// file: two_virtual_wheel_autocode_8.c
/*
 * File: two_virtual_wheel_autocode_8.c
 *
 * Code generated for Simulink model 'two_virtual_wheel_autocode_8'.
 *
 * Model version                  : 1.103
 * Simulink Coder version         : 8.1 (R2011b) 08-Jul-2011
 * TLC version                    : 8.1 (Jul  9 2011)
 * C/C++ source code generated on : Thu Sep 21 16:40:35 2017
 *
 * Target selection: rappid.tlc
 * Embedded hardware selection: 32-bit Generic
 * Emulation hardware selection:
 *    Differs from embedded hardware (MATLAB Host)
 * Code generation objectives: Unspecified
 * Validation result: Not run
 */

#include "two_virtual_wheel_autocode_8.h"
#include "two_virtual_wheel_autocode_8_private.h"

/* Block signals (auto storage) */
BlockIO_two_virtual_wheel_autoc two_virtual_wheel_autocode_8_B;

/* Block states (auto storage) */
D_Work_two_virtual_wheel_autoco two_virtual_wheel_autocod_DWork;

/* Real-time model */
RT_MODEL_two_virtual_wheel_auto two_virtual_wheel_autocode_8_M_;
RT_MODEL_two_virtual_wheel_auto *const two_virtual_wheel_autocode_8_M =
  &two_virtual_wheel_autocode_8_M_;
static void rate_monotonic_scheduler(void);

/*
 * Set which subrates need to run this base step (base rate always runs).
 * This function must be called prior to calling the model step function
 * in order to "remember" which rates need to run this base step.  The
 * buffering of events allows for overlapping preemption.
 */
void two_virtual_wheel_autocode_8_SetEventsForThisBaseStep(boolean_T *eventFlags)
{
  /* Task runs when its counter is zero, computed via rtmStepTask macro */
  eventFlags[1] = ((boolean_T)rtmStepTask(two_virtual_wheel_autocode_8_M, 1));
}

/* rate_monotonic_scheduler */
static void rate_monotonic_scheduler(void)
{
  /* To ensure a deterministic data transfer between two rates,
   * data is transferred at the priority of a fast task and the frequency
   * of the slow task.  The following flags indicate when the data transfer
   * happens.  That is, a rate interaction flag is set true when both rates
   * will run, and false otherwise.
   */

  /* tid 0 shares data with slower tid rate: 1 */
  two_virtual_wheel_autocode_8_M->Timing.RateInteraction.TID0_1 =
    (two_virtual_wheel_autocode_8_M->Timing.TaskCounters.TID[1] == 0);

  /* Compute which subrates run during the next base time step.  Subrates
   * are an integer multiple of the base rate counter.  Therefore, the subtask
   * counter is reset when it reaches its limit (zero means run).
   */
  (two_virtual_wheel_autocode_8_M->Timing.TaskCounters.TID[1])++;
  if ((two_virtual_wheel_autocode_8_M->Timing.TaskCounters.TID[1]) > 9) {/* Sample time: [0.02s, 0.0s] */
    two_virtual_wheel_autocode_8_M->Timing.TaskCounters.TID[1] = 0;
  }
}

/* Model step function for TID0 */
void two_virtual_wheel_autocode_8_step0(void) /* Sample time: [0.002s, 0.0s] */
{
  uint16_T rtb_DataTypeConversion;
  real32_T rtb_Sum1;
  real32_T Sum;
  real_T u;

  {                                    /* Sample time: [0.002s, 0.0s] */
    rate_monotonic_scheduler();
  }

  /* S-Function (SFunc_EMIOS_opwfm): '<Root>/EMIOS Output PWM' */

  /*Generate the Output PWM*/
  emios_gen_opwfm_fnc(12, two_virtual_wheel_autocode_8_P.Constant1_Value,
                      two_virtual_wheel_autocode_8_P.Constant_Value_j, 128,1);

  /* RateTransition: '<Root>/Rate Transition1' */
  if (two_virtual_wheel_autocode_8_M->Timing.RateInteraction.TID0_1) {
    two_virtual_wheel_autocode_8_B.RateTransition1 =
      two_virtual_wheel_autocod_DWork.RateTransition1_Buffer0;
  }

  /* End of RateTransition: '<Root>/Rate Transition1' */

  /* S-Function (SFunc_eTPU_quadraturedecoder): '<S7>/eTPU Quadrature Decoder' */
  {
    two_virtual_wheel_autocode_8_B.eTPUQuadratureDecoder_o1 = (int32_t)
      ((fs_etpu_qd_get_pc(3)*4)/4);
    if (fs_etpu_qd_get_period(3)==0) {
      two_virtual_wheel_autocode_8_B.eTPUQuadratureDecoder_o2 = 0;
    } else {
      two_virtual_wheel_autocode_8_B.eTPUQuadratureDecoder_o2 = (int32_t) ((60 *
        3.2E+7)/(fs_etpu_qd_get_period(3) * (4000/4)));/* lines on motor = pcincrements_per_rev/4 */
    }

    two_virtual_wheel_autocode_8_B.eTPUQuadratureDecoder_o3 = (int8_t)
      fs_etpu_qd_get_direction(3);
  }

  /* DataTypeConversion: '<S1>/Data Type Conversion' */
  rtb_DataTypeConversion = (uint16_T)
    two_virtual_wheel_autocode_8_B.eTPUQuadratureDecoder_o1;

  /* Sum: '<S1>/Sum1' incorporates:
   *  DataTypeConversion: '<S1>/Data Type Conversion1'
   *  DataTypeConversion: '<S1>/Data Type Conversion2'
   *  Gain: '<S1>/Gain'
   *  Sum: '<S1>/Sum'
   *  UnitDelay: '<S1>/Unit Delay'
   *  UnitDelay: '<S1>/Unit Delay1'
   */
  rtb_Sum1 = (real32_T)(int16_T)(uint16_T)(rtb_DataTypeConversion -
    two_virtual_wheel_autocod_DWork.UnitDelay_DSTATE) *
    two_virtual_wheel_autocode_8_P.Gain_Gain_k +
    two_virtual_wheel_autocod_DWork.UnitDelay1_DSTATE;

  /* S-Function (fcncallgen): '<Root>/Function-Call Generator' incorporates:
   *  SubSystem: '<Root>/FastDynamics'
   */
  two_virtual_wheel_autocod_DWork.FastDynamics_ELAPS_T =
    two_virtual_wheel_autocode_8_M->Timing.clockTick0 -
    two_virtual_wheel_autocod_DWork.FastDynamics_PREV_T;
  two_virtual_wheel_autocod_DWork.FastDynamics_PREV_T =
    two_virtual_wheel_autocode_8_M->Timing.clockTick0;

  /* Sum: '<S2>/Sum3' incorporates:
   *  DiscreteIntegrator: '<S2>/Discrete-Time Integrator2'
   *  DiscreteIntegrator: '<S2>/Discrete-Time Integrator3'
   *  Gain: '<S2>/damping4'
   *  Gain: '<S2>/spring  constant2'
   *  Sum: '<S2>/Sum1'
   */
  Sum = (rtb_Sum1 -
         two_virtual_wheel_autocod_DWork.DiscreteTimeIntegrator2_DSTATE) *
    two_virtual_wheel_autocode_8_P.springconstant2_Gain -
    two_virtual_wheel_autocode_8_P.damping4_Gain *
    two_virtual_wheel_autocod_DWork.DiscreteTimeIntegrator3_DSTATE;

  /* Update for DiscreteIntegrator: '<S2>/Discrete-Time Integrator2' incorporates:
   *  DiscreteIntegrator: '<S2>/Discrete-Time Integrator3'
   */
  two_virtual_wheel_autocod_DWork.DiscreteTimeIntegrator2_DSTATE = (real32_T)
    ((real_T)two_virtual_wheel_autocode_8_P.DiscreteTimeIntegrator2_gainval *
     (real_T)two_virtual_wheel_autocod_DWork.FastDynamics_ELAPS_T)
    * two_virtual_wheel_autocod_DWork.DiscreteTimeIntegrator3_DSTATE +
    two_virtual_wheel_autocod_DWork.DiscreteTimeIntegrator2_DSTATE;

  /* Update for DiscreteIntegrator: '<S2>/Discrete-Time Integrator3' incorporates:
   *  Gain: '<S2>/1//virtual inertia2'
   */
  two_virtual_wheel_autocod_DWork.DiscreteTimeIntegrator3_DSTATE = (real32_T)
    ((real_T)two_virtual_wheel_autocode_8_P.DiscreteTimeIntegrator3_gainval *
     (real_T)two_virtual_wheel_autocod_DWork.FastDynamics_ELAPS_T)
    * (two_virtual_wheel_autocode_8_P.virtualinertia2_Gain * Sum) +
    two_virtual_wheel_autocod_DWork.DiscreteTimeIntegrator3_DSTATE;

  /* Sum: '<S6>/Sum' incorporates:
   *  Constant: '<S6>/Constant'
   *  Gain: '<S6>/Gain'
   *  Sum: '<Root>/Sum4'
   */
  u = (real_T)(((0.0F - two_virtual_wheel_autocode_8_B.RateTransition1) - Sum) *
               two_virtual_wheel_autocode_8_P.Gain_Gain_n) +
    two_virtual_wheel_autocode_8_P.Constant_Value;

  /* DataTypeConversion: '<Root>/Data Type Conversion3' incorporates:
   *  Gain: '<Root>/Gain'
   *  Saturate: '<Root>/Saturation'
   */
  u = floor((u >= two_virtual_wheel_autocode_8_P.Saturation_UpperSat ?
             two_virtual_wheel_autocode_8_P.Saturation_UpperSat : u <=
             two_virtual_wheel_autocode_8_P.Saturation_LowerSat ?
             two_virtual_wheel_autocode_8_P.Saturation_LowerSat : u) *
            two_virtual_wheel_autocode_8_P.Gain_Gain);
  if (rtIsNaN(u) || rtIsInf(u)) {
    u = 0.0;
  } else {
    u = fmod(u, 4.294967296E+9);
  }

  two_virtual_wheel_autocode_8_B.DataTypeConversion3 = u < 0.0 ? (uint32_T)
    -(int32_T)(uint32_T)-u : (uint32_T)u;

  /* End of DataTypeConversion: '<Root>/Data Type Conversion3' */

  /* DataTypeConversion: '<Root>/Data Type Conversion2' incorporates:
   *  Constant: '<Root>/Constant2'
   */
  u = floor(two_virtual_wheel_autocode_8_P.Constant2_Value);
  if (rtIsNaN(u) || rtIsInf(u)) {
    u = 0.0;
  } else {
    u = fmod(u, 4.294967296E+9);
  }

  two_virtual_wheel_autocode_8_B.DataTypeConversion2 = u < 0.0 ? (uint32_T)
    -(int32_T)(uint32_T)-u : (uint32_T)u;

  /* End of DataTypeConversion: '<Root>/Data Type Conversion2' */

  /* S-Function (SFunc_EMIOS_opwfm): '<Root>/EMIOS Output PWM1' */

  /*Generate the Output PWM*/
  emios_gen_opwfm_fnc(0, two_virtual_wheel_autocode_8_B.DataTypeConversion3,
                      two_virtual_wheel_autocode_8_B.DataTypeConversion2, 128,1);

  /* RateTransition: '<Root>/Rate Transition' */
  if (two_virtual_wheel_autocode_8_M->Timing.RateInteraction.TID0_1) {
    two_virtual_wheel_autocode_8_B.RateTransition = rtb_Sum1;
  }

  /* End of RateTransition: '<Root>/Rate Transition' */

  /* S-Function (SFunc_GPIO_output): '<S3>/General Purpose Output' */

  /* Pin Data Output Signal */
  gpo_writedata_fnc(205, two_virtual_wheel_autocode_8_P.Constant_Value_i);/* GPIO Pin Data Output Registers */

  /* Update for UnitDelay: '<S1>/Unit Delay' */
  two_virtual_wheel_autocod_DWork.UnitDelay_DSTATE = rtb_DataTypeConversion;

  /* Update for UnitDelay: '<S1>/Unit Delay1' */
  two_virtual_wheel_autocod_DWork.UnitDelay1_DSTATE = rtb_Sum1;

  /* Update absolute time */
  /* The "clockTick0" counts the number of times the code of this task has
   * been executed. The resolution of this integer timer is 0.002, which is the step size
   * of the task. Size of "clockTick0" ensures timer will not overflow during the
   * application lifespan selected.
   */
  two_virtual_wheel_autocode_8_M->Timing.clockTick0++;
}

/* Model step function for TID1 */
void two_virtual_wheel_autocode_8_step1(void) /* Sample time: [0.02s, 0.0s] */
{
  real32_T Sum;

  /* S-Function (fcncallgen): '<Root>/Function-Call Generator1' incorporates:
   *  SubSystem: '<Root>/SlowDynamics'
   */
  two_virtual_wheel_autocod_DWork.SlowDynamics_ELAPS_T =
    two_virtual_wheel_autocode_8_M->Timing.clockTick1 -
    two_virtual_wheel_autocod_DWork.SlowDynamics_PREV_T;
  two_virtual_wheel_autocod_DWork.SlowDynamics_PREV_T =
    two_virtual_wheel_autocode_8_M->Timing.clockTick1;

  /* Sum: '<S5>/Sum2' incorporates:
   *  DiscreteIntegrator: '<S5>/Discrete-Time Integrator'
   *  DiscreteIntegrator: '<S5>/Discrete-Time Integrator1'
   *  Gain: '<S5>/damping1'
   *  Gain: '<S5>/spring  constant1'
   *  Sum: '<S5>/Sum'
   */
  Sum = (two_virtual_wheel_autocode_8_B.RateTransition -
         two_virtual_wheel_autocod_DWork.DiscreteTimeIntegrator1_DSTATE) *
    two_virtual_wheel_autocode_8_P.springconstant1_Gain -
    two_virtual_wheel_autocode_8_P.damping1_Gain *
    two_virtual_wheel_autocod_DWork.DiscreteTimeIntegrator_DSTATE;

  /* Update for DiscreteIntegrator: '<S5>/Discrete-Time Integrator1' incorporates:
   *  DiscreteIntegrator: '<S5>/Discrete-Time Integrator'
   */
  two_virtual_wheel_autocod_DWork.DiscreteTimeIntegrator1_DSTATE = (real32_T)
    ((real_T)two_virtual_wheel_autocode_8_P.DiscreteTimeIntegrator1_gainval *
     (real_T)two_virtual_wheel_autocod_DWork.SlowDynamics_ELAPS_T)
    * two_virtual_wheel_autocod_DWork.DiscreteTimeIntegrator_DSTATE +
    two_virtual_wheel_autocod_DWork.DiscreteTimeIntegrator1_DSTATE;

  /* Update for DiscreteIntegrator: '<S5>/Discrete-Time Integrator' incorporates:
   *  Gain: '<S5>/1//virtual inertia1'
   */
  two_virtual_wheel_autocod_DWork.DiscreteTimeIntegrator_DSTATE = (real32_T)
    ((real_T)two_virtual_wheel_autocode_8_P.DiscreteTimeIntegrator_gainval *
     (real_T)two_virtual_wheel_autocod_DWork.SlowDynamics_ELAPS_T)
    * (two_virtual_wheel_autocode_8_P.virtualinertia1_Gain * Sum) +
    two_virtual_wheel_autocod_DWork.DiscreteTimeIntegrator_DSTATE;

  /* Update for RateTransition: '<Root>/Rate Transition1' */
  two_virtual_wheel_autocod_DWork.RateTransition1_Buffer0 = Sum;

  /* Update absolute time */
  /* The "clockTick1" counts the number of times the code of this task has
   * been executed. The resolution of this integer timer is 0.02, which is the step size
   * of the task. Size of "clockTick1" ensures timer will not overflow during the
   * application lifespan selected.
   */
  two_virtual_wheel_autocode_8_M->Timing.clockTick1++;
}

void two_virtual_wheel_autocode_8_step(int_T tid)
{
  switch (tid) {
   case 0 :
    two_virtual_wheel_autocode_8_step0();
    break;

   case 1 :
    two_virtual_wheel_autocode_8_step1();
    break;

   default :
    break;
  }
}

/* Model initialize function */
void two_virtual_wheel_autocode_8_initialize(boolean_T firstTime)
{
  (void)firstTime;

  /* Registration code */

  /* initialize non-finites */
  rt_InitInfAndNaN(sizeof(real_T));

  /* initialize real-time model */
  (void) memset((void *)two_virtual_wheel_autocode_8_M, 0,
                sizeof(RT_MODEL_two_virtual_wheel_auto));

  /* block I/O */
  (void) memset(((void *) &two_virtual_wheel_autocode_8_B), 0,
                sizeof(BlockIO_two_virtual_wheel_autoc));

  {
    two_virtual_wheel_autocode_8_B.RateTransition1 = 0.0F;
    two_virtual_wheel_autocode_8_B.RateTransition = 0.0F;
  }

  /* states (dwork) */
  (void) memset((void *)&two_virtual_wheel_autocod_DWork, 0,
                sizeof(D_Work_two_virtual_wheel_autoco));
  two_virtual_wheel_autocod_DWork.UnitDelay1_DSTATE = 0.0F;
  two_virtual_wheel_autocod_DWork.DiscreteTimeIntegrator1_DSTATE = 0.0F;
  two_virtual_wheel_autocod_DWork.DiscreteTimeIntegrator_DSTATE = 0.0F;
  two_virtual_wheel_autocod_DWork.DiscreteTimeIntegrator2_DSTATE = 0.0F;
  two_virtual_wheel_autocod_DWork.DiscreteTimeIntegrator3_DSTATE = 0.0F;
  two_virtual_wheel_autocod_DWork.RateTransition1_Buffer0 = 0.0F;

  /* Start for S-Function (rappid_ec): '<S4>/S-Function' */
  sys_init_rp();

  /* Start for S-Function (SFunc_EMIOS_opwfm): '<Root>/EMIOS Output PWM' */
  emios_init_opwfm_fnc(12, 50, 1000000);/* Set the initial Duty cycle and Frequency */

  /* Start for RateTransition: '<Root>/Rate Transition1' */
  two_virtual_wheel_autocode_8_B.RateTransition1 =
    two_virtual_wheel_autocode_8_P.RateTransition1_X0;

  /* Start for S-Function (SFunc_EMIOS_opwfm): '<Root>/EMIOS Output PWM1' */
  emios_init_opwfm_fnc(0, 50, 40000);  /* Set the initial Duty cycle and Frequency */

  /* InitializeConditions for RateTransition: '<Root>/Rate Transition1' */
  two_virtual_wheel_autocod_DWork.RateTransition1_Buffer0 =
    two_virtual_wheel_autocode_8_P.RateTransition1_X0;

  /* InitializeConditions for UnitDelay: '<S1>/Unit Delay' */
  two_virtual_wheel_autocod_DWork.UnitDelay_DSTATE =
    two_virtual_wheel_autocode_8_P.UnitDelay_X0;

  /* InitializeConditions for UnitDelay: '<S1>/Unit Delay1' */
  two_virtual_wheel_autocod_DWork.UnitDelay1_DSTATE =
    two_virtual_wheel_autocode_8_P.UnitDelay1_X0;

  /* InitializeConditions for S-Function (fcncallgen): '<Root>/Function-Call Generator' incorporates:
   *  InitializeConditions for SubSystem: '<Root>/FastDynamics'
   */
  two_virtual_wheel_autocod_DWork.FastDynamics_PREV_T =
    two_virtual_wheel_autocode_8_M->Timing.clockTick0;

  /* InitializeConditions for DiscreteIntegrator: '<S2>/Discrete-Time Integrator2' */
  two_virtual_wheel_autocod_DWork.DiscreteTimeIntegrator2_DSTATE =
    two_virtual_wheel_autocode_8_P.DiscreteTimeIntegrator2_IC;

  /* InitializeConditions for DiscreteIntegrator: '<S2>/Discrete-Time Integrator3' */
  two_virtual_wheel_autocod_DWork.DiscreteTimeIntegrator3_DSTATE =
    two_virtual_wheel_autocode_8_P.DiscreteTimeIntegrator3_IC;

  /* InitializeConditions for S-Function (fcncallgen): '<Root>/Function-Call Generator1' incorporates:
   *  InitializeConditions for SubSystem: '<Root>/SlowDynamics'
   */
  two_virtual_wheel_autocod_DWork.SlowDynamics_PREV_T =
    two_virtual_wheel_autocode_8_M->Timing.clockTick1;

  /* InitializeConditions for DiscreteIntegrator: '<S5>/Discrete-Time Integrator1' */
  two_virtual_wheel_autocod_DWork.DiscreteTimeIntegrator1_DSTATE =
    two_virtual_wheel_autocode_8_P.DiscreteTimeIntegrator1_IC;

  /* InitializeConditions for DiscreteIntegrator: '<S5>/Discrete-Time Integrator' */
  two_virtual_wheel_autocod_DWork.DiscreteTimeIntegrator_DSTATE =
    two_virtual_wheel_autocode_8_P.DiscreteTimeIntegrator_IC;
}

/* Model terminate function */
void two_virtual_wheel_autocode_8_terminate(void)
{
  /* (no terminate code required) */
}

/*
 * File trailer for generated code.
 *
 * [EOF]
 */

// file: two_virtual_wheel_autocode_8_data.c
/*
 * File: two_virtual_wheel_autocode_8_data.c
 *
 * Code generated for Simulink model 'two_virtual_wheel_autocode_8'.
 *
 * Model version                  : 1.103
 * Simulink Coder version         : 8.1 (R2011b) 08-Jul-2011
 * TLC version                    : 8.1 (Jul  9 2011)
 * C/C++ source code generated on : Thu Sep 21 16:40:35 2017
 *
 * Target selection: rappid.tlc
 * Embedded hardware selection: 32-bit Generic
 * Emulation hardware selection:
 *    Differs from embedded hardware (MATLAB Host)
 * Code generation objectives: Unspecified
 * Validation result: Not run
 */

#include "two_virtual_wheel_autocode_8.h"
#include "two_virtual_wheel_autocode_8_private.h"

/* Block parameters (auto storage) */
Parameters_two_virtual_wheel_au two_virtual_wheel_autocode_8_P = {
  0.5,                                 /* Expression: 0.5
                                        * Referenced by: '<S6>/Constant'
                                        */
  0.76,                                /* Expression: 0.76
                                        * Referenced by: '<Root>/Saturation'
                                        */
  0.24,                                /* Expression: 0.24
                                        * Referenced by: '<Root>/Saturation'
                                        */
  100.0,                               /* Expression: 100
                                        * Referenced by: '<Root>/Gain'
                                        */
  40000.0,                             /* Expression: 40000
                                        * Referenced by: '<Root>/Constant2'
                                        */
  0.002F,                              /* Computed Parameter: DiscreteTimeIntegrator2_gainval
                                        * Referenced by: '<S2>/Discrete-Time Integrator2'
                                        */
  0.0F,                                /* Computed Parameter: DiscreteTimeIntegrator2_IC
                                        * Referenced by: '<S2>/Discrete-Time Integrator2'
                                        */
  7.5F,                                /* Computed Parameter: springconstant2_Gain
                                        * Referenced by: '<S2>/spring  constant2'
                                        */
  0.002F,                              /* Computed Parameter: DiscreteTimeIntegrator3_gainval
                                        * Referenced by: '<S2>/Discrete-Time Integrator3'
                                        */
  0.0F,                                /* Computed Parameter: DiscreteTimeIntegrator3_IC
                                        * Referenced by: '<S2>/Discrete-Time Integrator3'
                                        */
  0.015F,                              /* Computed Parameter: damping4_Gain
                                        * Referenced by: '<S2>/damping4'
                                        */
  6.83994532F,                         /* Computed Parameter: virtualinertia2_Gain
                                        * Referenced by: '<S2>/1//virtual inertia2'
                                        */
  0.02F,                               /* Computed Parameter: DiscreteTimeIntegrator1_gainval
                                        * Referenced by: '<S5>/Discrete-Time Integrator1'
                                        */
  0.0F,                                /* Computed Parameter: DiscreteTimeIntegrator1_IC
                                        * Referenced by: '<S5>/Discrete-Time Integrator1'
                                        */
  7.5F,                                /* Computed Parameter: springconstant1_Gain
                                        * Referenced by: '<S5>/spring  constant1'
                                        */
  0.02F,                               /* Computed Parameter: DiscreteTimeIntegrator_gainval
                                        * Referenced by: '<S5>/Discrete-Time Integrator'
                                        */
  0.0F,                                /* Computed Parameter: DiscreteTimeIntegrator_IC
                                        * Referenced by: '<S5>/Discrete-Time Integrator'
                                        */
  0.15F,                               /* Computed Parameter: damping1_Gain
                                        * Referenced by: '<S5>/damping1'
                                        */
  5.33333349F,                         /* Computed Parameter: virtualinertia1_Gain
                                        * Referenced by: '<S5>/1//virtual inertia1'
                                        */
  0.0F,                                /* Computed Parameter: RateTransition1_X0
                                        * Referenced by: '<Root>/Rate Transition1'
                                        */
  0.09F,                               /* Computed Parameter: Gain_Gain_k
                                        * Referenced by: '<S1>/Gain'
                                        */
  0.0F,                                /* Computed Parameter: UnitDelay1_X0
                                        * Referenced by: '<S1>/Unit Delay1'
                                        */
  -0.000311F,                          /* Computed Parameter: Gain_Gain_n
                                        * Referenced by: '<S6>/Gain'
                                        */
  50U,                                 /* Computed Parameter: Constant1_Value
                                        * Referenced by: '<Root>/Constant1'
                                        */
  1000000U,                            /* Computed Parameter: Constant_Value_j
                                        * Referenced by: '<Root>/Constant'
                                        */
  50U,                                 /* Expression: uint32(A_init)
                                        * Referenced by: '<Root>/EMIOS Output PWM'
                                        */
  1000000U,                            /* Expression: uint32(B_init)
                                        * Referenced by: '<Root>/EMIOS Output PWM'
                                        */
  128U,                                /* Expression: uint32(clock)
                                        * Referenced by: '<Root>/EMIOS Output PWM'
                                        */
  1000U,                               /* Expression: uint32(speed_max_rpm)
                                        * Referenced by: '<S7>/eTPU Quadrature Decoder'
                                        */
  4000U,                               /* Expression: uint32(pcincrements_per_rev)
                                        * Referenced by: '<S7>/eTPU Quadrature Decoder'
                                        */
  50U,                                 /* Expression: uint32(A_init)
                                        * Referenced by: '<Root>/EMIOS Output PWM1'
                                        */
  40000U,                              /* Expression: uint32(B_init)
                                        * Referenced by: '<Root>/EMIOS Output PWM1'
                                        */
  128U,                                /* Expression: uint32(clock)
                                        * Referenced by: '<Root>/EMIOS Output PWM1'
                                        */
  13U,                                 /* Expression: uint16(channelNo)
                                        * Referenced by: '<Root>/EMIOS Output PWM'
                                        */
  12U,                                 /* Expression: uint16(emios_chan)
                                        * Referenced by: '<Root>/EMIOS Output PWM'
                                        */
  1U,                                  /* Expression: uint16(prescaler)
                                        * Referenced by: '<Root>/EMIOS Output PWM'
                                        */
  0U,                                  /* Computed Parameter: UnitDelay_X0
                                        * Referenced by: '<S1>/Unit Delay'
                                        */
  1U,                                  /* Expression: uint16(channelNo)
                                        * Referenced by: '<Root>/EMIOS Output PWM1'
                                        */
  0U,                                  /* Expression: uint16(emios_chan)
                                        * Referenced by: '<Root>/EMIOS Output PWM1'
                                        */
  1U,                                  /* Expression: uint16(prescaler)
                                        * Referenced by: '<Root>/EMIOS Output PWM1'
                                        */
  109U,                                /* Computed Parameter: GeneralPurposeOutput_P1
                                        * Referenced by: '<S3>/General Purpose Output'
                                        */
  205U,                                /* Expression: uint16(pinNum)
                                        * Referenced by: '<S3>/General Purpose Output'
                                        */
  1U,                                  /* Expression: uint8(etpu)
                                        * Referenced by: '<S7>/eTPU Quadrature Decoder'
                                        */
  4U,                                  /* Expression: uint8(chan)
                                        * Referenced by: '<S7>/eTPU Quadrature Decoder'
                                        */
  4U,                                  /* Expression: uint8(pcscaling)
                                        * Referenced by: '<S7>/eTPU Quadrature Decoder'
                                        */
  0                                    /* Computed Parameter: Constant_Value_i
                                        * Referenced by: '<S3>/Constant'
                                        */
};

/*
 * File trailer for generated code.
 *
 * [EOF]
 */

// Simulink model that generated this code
simulink model "two_virtual_wheel_autocode_8"  (Simulink 7.8)
settings: Solver=FixedStepDiscrete  SolverMode=MultiTasking  StartTime=0.0  StopTime=tfinal  RelTol=1e-3
InitFcn:
  | two_virtual_wheel_params
undefined symbols (not defined in the file): b1, b2, DiscIntNeverNeededParam, Jw1, Jw2, k1, k2, SFunc_eTPU_quadraturedecoder_Script, SFunc_gpio_output_Script
libraries: rappid_ec_lib x2, simulink x2, rappid_lib x1

== system two_virtual_wheel_autocode_8 ==
  note: wheel position
  note: thetaz
  Constant : Constant  Value=1000000  OutDataTypeStr=uint32
  Constant1 : Constant  Value=50  OutDataTypeStr=uint32
  Constant2 : Constant  Value=40000
  ConversionSystem : Subsystem
  Data Type Conversion{,1..3} (4 alike) : DataTypeConversion  OutDataTypeStr=uint32
  EMIOS Output PWM : rappid_ec_lib/Peripheral Driver Blocks/eMIOS Blocks/EMIOS Output PWM  channelNo=12  emios_chan=12  A_init=50  B_init=1000000  clock=128  prescaler=1
  EMIOS Output PWM1 : rappid_ec_lib/Peripheral Driver Blocks/eMIOS Blocks/EMIOS Output PWM  channelNo=0  emios_chan=0  A_init=50  B_init=40000  clock=128  prescaler=1
  FastDynamics : Subsystem
  Function-Call Generator : simulink/Ports & Subsystems/Function-Call Generator  sample_time=0.002  numberOfIterations=1
  Function-Call Generator1 : simulink/Ports & Subsystems/Function-Call Generator  sample_time=0.02  numberOfIterations=1
  GPIO Blocks : Subsystem  AncestorBlock=rappid_ec_lib/Peripheral Driver Blocks/GPIO Blocks
  Gain : Gain  Gain=100
  RAppID-EC : rappid_lib/RAppID Initialization Blocks/RAppID-EC  Tag=RAppID  Priority=0  rtos=simpletarget  targetmcu=IntRAM  clockfrequency=128  basetaskpriority=20  systemcounter=0  systimer_isrpriority=1  systimer_period=0  isrstacksize=50  interruptdispatcher=None  stored_mdl_name=two_virtual_wheel_autocode_8
  Rate Transition : RateTransition
  Rate Transition1 : RateTransition
  Saturation : Saturate  UpperLimit=0.76  LowerLimit=0.24
  SlowDynamics : Subsystem
  Subsystem : Subsystem
  Sum4 : Sum  Inputs=-|-  SaturateOnIntegerOverflow=on  InputSameDT=on  OutDataTypeStr=Inherit: Same as first input
  Terminator : Terminator
  Terminator1 : Terminator
  eTPU Blocks : Subsystem  AncestorBlock=rappid_ec_lib/Peripheral Driver Blocks/eTPU Blocks
  wires:
  ConversionSystem/1(Out1) -> Rate Transition/1, FastDynamics/1(In1)
  Rate Transition1/1 -> Sum4/1
  Rate Transition/1 -> SlowDynamics/1(thetaz)
  SlowDynamics/1(torque1) -> Rate Transition1/1
  FastDynamics/1(torque2) -> Sum4/2
  Function-Call Generator1/1 -> SlowDynamics/Trigger
  Function-Call Generator/1 -> FastDynamics/Trigger
  Constant1/1 -> Data Type Conversion/1
  Data Type Conversion/1 -> EMIOS Output PWM/1
  Constant/1 -> Data Type Conversion1/1
  Data Type Conversion1/1 -> EMIOS Output PWM/2
  Subsystem/1(Out1) -> Saturation/1
  Saturation/1 -> Gain/1
  Constant2/1 -> Data Type Conversion2/1
  Data Type Conversion2/1 -> EMIOS Output PWM1/2
  Data Type Conversion3/1 -> EMIOS Output PWM1/1
  Gain/1 -> Data Type Conversion3/1
  Sum4/1 -> Subsystem/1(In1)
  eTPU Blocks/2(Out2) -> Terminator/1
  eTPU Blocks/3(Out3) -> Terminator1/1
  eTPU Blocks/1(Out1) -> ConversionSystem/1(In1)

== system two_virtual_wheel_autocode_8/ConversionSystem ==
  In1 : Inport
  Data Type Conversion : DataTypeConversion  OutDataTypeStr=uint16
  Data Type Conversion1 : DataTypeConversion  OutDataTypeStr=single
  Data Type Conversion2 : DataTypeConversion  OutDataTypeStr=int16
  Gain : Gain  Gain=0.09
  Sum : Sum  Inputs=|+-
  Sum1 : Sum  Inputs=|++  AccumDataTypeStr=single  OutDataTypeStr=single
  Unit Delay : UnitDelay  SampleTime=-1
  Unit Delay1 : UnitDelay  SampleTime=-1
  Out1 : Outport
  wires:
  Unit Delay/1 -> Sum/2
  Sum/1 -> Data Type Conversion2/1
  Data Type Conversion2/1 -> Data Type Conversion1/1
  Data Type Conversion1/1 -> Gain/1
  Gain/1 -> Sum1/1
  Sum1/1 -> Out1/1, Unit Delay1/1
  Data Type Conversion/1 -> Sum/1, Unit Delay/1
  In1/1 -> Data Type Conversion/1
  Unit Delay1/1 -> Sum1/2

== system two_virtual_wheel_autocode_8/FastDynamics ==
  note: Fast Dynamics
  note: thetaz
  note: theta2ddot
  note: theta2dot
  note: theta2
  In1 : Inport
  Trigger : TriggerPort  TriggerType=function-call  PortDimensions=1
  1/virtual inertia2 : Gain  Gain=1/Jw2  SaturateOnIntegerOverflow=on  OutDataTypeStr=Inherit: Same as input  ParamDataTypeStr=Inherit: Same as input
  Discrete-Time Integrator2 : DiscreteIntegrator  SampleTime=-1  ICPrevOutput=DiscIntNeverNeededParam  ICPrevScaledInput=DiscIntNeverNeededParam
  Discrete-Time Integrator3 : DiscreteIntegrator  SampleTime=-1  ICPrevOutput=DiscIntNeverNeededParam  ICPrevScaledInput=DiscIntNeverNeededParam
  Sum1 : Sum  Inputs=|+-  SaturateOnIntegerOverflow=on  InputSameDT=on  OutDataTypeStr=Inherit: Same as first input
  Sum3 : Sum  Inputs=|+-  SaturateOnIntegerOverflow=on  InputSameDT=on  OutDataTypeStr=Inherit: Same as first input
  damping4 : Gain  Gain=b2  SaturateOnIntegerOverflow=on  OutDataTypeStr=Inherit: Same as input  ParamDataTypeStr=Inherit: Same as input
  spring  constant2 : Gain  Gain=k2  SaturateOnIntegerOverflow=on  OutDataTypeStr=Inherit: Same as input  ParamDataTypeStr=Inherit: Same as input
  torque2 : Outport
  wires:
  spring  constant2/1 -> Sum3/1
  damping4/1 -> Sum3/2
  Sum3/1 -> torque2/1, 1/virtual inertia2/1
  Discrete-Time Integrator3/1 -> Discrete-Time Integrator2/1, damping4/1
  1/virtual inertia2/1 -> Discrete-Time Integrator3/1
  Sum1/1 -> spring  constant2/1
  Discrete-Time Integrator2/1 -> Sum1/2
  In1/1 -> Sum1/1

== system two_virtual_wheel_autocode_8/GPIO Blocks ==
  Constant : Constant  Value=0  OutDataTypeStr=boolean
  General Purpose Output : S-Function  InitFcn=SFunc_gpio_output_Script(bdroot(gcs)) ;  FunctionName=SFunc_GPIO_output  Parameters=char(gpoi_outputs),uint16(pinNum)  EnableBusSupport=off  mask(GPIO_Output){gpoi_outputs=205:   Primary Function "GPIO", pinNum=205}
      mask prompts: gpoi_outputs "Output Pin (GPO [ 0 - 213])"; pinNum "Pin Number"
      mask help: Select a General Purpose Output Pin as a Source (GPI [ 0 - 213]).
      mask init:
      | pinStr = get_param(gcb,'gpoi_outputs');
      | 
      | if strcmp(pinStr,'none')==0
      | 	pos =   findstr(pinStr,':');
      | 	pinVal = pinStr(1:pos(1)-1); 
      | 	set_param(gcb,'pinNum',pinVal);
      | 	st=['GPO [' pinVal, ']'];
      | else
      | 	set_param(gcb,'pinNum','');
      | 	st=['    No GPO Pin Selected'];
      | end
  wires:
  Constant/1 -> General Purpose Output/1

== system two_virtual_wheel_autocode_8/SlowDynamics ==
  note: Slow Dynamics
  note: theta1ddot
  note: theta1dot
  note: theta1
  thetaz : Inport
  Trigger : TriggerPort  TriggerType=function-call  PortDimensions=1
  1/virtual inertia1 : Gain  Gain=1/Jw1  SaturateOnIntegerOverflow=on  OutDataTypeStr=Inherit: Same as input  ParamDataTypeStr=Inherit: Same as input
  Discrete-Time Integrator : DiscreteIntegrator  SampleTime=-1  ICPrevOutput=DiscIntNeverNeededParam  ICPrevScaledInput=DiscIntNeverNeededParam
  Discrete-Time Integrator1 : DiscreteIntegrator  SampleTime=-1  ICPrevOutput=DiscIntNeverNeededParam  ICPrevScaledInput=DiscIntNeverNeededParam
  Sum : Sum  Inputs=|+-  SaturateOnIntegerOverflow=on  InputSameDT=on  OutDataTypeStr=Inherit: Same as first input
  Sum2 : Sum  Inputs=|+-  SaturateOnIntegerOverflow=on  InputSameDT=on  OutDataTypeStr=Inherit: Same as first input
  To Workspace : ToWorkspace  VariableName=theta1  SampleTime=-1  SaveFormat=Structure With Time
  To Workspace1 : ToWorkspace  VariableName=theta1dot  SampleTime=-1  SaveFormat=Structure With Time
  To Workspace2 : ToWorkspace  VariableName=wheel1_torque  SampleTime=-1  SaveFormat=Structure With Time
  damping1 : Gain  Gain=b1  SaturateOnIntegerOverflow=on  OutDataTypeStr=Inherit: Same as input  ParamDataTypeStr=Inherit: Same as input
  spring  constant1 : Gain  Gain=k1  SaturateOnIntegerOverflow=on  OutDataTypeStr=Inherit: Same as input  ParamDataTypeStr=Inherit: Same as input
  torque1 : Outport
  wires:
  damping1/1 -> Sum2/2
  Sum2/1 -> 1/virtual inertia1/1, To Workspace2/1, torque1/1
  spring  constant1/1 -> Sum2/1
  Discrete-Time Integrator/1 -> Discrete-Time Integrator1/1, damping1/1, To Workspace1/1
  1/virtual inertia1/1 -> Discrete-Time Integrator/1
  Sum/1 -> spring  constant1/1
  Discrete-Time Integrator1/1 -> Sum/2, To Workspace/1
  thetaz/1 -> Sum/1

== system two_virtual_wheel_autocode_8/Subsystem ==
  In1 : Inport
  Constant : Constant  Value=0.5
  Gain : Gain  Gain=-3.11e-4
  Sum : Sum  Inputs=|++
  Out1 : Outport
  wires:
  Gain/1 -> Sum/1
  Constant/1 -> Sum/2
  In1/1 -> Gain/1
  Sum/1 -> Out1/1

== system two_virtual_wheel_autocode_8/eTPU Blocks ==
  eTPU Quadrature Decoder : S-Function  Priority=-100000000  InitFcn=SFunc_eTPU_quadraturedecoder_Script;  FunctionName=SFunc_eTPU_quadraturedecoder  Parameters=uint8(etpu) ,uint8(chan),uint32(speed_max_rpm),uint32(pcincrements_per_rev),uint8(pcscaling)  EnableBusSupport=off  mask(SFunc_eTPU_quadraturedecoder){etpu=0, chan=3, speed_max_rpm=1000, pcincrements_per_rev=4000, pcscaling=4}
      mask prompts: chan "Channel"; speed_max_rpm "Max Speed (rpm)"; pcincrements_per_rev "Position Counter Increments per Revolution (4 X lines on motor)"; pcscaling "Position Count Scaling"
      mask help: Implements the quadrature decoder functionality based on phase A and phase B encoder signals typicaly used for controlling DC motors. Outputs Position Counts (24-bit counter which rolls over on overflow), Angular Velocity in rpm and Direction of motor at every time-step. Right-click on the block and see block help for usage details
      mask init:
      | etpudm = ['eTPU: ' get_param(gcb,'etpu')];
      | chandm = ['Channel: ' num2str(str2num(get_param(gcb,'chan')) + (str2num(get_param(gcb,'etpu'))*64))];
      | secchandm = ['Secondary Channel: ' num2str(str2num(get_param(gcb,'chan')) + (str2num(get_param(gcb,'etpu'))*64)+1)];
      | speed_max_rpmdm = ['Max Speed (rpm): ' num2str(get_value(get_param(gcb,'speed_max_rpm')))];
      | pcincrements_per_revdm = ['Position Counter Increments per Revolution (4 X lines on motor): ' num2str(get_value(get_param(gcb,'pcincrements_per_rev')))];
      | pcscalingdm = ['Position Counts Scaling): PositionCounts X ' get_param(gcb,'pcscaling')];
      | rp_set_cur_model(bdroot(gcb));
  Out1 : Outport
  Out2 : Outport  Port=2
  Out3 : Outport  Port=3
  wires:
  eTPU Quadrature Decoder/1 -> Out1/1
  eTPU Quadrature Decoder/2 -> Out2/1
  eTPU Quadrature Decoder/3 -> Out3/1
